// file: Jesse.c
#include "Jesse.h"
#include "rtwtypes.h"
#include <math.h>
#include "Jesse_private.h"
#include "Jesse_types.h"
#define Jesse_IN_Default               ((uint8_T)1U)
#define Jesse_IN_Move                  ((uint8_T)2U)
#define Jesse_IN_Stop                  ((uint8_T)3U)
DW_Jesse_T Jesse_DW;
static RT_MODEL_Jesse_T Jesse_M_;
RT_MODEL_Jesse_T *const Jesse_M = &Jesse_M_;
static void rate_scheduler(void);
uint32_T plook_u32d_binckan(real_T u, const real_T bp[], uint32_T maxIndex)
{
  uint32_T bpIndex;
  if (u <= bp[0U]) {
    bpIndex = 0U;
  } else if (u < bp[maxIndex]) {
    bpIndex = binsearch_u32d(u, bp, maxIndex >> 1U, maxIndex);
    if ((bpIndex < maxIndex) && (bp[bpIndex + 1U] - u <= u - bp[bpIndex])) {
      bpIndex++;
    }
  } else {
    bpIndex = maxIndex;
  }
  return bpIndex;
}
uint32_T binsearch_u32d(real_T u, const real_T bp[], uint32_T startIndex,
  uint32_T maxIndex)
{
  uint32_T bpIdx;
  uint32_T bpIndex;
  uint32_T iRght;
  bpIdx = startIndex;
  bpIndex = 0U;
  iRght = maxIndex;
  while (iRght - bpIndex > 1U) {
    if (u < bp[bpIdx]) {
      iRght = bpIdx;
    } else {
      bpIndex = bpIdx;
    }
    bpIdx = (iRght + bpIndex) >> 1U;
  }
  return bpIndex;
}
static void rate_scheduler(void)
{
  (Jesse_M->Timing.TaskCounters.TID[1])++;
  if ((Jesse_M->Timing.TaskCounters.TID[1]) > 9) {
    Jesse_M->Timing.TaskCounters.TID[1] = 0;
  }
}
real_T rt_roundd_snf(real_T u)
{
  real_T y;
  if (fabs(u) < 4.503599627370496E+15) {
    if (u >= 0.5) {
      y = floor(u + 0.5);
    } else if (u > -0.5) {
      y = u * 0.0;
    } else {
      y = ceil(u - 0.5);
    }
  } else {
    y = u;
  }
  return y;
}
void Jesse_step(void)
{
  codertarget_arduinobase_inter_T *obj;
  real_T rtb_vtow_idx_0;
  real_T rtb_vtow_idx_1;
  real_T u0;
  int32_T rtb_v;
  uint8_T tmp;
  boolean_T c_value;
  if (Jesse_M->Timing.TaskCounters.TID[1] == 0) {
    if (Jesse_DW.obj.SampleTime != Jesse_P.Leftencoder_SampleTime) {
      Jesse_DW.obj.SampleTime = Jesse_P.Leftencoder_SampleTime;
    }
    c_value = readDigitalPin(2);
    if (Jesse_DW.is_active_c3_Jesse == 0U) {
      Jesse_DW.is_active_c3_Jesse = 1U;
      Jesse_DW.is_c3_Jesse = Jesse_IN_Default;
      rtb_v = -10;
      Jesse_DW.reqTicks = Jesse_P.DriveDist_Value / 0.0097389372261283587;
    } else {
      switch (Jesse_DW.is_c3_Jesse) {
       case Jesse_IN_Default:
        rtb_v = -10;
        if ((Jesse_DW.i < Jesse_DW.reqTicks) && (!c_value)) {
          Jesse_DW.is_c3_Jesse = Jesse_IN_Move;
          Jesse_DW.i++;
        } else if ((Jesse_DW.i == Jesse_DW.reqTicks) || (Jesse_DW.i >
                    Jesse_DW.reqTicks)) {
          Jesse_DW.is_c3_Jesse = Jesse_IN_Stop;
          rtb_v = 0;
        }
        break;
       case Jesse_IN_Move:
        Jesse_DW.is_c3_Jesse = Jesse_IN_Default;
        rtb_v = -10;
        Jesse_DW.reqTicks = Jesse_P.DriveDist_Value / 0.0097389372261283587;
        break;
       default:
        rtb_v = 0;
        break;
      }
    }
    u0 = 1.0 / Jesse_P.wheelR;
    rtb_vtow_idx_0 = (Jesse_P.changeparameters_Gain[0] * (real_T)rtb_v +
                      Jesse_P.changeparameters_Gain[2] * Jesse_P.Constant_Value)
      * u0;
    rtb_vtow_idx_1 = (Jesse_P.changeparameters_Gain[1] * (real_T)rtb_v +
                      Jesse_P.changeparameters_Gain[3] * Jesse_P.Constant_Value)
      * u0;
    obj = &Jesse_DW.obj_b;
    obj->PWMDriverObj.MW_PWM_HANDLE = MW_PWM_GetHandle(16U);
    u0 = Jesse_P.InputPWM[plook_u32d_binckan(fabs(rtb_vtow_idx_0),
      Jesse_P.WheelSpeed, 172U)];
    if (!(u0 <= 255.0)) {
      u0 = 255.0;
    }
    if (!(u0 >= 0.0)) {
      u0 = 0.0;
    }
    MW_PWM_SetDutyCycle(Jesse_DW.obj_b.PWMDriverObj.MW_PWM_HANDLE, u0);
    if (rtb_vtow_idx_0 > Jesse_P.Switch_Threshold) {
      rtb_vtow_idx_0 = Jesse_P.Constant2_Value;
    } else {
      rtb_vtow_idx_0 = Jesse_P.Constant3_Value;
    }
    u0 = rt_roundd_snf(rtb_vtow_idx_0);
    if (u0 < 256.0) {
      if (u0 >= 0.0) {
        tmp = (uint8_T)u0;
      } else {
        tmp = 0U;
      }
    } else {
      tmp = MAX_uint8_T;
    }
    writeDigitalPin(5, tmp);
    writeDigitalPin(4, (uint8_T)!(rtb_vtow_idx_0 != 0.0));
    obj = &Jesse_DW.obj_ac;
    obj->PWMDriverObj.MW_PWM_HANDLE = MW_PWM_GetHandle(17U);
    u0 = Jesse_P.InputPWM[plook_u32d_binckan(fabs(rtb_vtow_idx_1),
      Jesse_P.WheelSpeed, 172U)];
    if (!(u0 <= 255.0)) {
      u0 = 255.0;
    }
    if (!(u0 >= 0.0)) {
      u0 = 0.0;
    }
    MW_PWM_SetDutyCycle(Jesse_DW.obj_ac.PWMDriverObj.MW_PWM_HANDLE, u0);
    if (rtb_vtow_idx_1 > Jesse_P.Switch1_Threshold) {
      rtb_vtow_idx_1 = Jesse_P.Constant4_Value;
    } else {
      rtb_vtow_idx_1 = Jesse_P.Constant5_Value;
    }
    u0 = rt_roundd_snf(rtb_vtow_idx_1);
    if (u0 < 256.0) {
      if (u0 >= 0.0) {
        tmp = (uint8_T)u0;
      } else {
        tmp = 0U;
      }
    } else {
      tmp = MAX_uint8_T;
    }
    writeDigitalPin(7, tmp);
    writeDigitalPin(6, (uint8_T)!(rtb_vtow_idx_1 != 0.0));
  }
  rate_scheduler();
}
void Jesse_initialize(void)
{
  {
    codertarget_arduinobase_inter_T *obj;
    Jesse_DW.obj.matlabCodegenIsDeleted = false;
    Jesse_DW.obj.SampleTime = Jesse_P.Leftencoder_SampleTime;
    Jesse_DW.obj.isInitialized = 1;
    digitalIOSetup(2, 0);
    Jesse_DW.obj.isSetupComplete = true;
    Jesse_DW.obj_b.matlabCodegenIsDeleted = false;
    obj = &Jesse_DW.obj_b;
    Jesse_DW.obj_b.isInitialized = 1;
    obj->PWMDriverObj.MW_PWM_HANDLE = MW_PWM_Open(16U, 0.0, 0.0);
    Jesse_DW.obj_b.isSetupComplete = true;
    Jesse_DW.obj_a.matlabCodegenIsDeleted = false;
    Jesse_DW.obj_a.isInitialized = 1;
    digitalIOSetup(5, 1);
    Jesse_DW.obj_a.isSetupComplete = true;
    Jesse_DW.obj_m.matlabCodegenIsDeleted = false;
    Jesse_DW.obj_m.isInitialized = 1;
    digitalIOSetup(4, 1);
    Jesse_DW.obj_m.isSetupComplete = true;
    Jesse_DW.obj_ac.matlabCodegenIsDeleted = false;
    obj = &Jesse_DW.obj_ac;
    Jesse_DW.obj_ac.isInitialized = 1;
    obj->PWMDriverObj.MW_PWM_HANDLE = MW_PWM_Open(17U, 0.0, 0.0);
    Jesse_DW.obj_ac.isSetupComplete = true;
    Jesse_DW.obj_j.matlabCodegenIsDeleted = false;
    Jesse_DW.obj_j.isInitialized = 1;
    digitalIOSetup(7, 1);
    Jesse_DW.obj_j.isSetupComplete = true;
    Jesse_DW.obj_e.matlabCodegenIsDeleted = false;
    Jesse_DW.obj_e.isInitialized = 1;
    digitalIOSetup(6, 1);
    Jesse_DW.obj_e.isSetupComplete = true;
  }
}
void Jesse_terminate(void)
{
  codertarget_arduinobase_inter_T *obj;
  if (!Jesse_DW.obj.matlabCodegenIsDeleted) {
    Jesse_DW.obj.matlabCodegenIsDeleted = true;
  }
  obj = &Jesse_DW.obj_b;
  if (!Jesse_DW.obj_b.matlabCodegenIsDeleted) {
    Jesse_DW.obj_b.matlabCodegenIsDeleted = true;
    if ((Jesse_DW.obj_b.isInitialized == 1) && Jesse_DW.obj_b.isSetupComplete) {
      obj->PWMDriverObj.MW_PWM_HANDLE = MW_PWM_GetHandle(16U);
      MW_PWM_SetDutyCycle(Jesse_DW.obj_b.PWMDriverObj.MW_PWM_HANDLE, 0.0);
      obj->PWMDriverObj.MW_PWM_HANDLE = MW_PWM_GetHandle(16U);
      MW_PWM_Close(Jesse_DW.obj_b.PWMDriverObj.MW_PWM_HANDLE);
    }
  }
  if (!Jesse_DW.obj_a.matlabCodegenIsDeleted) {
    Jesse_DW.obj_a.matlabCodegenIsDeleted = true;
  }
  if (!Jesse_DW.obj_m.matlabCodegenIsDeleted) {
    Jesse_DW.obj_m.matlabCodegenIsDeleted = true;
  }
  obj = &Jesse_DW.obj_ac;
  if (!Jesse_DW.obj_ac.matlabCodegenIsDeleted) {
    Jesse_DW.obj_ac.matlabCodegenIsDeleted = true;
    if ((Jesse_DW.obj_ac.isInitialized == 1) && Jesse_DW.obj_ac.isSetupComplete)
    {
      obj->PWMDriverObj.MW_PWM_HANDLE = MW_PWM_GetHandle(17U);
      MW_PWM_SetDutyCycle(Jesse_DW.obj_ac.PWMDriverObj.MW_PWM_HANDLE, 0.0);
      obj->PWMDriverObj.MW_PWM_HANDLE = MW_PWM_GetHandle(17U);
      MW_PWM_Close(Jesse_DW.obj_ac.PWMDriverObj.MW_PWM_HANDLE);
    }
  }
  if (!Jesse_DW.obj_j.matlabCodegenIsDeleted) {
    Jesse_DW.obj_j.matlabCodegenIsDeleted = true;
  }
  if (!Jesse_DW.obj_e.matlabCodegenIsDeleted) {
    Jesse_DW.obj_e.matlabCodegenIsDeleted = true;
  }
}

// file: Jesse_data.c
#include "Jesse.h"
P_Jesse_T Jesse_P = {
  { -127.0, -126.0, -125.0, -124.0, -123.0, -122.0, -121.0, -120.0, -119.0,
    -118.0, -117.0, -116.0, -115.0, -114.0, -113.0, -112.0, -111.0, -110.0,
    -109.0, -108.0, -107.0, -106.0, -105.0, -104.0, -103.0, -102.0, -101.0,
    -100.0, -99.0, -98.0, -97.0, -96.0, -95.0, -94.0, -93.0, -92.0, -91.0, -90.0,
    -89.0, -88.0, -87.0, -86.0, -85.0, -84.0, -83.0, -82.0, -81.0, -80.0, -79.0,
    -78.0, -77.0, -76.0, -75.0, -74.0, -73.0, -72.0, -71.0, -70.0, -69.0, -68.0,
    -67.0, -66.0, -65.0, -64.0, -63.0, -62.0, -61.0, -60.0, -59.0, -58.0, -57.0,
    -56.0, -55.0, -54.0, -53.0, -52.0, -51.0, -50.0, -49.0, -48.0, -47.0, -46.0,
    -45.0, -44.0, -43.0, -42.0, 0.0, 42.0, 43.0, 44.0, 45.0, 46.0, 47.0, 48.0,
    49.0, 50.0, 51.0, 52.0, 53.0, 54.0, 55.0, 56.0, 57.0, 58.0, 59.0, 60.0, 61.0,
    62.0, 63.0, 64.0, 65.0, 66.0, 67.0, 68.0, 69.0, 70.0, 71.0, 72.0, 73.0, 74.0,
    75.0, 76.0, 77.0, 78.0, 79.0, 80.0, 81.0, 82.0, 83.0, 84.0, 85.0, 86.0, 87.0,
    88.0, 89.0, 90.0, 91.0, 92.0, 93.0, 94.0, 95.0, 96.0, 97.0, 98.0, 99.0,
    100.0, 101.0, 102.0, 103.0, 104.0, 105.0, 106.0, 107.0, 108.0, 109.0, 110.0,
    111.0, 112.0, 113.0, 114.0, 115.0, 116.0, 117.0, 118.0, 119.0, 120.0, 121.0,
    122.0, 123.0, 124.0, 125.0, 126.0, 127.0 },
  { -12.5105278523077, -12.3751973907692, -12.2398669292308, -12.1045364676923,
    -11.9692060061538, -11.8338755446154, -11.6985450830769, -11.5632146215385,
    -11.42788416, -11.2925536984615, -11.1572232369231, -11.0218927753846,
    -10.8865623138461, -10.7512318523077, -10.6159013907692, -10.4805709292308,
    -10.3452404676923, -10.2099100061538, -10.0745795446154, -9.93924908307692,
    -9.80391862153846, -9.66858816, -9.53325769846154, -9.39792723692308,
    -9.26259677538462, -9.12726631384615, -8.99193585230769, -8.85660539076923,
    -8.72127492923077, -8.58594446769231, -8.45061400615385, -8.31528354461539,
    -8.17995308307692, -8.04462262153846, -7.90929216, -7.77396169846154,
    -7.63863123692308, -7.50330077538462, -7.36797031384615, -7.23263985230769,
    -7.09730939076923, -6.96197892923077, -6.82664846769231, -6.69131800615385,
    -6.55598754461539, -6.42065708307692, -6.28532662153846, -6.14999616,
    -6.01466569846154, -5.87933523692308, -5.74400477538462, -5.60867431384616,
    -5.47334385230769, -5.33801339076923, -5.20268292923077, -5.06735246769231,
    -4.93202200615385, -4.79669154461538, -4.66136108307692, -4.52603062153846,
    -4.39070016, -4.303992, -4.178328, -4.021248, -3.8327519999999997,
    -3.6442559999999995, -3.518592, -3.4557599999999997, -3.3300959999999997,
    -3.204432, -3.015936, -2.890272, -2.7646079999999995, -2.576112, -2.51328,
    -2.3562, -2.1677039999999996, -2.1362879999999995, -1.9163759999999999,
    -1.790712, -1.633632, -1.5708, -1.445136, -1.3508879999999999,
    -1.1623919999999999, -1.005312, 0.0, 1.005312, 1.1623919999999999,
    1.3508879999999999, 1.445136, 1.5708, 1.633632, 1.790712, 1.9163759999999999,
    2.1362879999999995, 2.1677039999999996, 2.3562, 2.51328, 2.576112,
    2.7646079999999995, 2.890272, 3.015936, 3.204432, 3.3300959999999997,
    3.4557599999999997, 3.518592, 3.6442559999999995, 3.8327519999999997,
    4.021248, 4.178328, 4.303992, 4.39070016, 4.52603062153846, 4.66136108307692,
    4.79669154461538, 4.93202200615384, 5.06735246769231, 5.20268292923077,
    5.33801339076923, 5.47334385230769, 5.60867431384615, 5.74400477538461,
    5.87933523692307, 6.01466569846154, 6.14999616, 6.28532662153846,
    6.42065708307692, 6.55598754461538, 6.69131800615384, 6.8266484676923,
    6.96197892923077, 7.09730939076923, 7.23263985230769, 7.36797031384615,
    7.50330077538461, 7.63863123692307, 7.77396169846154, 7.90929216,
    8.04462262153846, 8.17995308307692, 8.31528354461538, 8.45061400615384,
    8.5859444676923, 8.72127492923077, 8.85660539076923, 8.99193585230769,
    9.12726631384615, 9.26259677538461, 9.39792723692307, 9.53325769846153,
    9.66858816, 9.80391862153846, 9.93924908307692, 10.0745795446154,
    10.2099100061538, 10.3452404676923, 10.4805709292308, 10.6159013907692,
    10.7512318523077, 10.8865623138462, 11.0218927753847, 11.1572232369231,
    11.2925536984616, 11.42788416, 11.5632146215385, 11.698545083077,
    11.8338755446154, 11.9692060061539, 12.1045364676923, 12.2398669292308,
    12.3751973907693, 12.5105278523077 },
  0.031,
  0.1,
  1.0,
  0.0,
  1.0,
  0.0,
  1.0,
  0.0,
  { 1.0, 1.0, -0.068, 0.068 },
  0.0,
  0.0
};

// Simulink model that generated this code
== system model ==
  PWM#1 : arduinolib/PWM  pinNumber=16  <- 1: Lookup_nD#1
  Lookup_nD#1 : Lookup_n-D  BreakpointsForDimension1=WheelSpeed  Table=InputPWM  InterpMethod=Nearest  <- 1: Abs#1
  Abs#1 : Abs  <- 1: Towlwr#1
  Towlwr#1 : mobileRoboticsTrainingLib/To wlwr  <- 1: Stateflowchart#1, 2: Constant
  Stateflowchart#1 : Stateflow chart  <- 1: DriveDist, 2: Leftencoder
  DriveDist : Constant
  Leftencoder : arduinolib/Digital Input  pinNumber=2
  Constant : Constant  Value=0
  DigitalOutput#1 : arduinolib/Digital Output  pinNumber=5  <- 1: Switch
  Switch : Switch  Criteria=u2 > Threshold  <- 1: Constant2, 2: Towlwr#1, 3: Constant3
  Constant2 : Constant
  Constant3 : Constant  Value=0
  DigitalOutput#2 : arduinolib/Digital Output  pinNumber=4  <- 1: Logic#1
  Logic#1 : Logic  Operator=NOT  <- 1: Switch
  PWM#2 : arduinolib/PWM  pinNumber=17  <- 1: Lookup_nD#2
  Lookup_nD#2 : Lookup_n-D  BreakpointsForDimension1=WheelSpeed  Table=InputPWM  InterpMethod=Nearest  <- 1: Abs#2
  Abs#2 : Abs  <- 1: Towlwr#1/2
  DigitalOutput#3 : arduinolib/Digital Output  pinNumber=7  <- 1: Switch1
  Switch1 : Switch  Criteria=u2 > Threshold  <- 1: Constant4, 2: Towlwr#1/2, 3: Constant5
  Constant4 : Constant
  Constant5 : Constant  Value=0
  DigitalOutput#4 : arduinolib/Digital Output  pinNumber=6  <- 1: Logic#2
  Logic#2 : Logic  Operator=NOT  <- 1: Switch1
== stateflow chart Stateflowchart#1 ==
  state Default
    entry:
    ticks;
    i;
    v=-10;
    dist1Tick=(pi*0.031)/10
    reqTicks=reqDist/dist1Tick;
  state Stop
    entry:
    v=0;
  state Move
    entry:
    v=-10;
    i=i+1;
    x=i;
  (default) -> Default
  Default -> Stop [order 2] : [i==reqTicks | i>reqTicks]
  Move -> Default
  Default -> Move [order 1] : [i<reqTicks && ticks==0]
  data: reqDist input; ticks input; v output; dist1Tick local; reqTicks local; i local =0; x output
